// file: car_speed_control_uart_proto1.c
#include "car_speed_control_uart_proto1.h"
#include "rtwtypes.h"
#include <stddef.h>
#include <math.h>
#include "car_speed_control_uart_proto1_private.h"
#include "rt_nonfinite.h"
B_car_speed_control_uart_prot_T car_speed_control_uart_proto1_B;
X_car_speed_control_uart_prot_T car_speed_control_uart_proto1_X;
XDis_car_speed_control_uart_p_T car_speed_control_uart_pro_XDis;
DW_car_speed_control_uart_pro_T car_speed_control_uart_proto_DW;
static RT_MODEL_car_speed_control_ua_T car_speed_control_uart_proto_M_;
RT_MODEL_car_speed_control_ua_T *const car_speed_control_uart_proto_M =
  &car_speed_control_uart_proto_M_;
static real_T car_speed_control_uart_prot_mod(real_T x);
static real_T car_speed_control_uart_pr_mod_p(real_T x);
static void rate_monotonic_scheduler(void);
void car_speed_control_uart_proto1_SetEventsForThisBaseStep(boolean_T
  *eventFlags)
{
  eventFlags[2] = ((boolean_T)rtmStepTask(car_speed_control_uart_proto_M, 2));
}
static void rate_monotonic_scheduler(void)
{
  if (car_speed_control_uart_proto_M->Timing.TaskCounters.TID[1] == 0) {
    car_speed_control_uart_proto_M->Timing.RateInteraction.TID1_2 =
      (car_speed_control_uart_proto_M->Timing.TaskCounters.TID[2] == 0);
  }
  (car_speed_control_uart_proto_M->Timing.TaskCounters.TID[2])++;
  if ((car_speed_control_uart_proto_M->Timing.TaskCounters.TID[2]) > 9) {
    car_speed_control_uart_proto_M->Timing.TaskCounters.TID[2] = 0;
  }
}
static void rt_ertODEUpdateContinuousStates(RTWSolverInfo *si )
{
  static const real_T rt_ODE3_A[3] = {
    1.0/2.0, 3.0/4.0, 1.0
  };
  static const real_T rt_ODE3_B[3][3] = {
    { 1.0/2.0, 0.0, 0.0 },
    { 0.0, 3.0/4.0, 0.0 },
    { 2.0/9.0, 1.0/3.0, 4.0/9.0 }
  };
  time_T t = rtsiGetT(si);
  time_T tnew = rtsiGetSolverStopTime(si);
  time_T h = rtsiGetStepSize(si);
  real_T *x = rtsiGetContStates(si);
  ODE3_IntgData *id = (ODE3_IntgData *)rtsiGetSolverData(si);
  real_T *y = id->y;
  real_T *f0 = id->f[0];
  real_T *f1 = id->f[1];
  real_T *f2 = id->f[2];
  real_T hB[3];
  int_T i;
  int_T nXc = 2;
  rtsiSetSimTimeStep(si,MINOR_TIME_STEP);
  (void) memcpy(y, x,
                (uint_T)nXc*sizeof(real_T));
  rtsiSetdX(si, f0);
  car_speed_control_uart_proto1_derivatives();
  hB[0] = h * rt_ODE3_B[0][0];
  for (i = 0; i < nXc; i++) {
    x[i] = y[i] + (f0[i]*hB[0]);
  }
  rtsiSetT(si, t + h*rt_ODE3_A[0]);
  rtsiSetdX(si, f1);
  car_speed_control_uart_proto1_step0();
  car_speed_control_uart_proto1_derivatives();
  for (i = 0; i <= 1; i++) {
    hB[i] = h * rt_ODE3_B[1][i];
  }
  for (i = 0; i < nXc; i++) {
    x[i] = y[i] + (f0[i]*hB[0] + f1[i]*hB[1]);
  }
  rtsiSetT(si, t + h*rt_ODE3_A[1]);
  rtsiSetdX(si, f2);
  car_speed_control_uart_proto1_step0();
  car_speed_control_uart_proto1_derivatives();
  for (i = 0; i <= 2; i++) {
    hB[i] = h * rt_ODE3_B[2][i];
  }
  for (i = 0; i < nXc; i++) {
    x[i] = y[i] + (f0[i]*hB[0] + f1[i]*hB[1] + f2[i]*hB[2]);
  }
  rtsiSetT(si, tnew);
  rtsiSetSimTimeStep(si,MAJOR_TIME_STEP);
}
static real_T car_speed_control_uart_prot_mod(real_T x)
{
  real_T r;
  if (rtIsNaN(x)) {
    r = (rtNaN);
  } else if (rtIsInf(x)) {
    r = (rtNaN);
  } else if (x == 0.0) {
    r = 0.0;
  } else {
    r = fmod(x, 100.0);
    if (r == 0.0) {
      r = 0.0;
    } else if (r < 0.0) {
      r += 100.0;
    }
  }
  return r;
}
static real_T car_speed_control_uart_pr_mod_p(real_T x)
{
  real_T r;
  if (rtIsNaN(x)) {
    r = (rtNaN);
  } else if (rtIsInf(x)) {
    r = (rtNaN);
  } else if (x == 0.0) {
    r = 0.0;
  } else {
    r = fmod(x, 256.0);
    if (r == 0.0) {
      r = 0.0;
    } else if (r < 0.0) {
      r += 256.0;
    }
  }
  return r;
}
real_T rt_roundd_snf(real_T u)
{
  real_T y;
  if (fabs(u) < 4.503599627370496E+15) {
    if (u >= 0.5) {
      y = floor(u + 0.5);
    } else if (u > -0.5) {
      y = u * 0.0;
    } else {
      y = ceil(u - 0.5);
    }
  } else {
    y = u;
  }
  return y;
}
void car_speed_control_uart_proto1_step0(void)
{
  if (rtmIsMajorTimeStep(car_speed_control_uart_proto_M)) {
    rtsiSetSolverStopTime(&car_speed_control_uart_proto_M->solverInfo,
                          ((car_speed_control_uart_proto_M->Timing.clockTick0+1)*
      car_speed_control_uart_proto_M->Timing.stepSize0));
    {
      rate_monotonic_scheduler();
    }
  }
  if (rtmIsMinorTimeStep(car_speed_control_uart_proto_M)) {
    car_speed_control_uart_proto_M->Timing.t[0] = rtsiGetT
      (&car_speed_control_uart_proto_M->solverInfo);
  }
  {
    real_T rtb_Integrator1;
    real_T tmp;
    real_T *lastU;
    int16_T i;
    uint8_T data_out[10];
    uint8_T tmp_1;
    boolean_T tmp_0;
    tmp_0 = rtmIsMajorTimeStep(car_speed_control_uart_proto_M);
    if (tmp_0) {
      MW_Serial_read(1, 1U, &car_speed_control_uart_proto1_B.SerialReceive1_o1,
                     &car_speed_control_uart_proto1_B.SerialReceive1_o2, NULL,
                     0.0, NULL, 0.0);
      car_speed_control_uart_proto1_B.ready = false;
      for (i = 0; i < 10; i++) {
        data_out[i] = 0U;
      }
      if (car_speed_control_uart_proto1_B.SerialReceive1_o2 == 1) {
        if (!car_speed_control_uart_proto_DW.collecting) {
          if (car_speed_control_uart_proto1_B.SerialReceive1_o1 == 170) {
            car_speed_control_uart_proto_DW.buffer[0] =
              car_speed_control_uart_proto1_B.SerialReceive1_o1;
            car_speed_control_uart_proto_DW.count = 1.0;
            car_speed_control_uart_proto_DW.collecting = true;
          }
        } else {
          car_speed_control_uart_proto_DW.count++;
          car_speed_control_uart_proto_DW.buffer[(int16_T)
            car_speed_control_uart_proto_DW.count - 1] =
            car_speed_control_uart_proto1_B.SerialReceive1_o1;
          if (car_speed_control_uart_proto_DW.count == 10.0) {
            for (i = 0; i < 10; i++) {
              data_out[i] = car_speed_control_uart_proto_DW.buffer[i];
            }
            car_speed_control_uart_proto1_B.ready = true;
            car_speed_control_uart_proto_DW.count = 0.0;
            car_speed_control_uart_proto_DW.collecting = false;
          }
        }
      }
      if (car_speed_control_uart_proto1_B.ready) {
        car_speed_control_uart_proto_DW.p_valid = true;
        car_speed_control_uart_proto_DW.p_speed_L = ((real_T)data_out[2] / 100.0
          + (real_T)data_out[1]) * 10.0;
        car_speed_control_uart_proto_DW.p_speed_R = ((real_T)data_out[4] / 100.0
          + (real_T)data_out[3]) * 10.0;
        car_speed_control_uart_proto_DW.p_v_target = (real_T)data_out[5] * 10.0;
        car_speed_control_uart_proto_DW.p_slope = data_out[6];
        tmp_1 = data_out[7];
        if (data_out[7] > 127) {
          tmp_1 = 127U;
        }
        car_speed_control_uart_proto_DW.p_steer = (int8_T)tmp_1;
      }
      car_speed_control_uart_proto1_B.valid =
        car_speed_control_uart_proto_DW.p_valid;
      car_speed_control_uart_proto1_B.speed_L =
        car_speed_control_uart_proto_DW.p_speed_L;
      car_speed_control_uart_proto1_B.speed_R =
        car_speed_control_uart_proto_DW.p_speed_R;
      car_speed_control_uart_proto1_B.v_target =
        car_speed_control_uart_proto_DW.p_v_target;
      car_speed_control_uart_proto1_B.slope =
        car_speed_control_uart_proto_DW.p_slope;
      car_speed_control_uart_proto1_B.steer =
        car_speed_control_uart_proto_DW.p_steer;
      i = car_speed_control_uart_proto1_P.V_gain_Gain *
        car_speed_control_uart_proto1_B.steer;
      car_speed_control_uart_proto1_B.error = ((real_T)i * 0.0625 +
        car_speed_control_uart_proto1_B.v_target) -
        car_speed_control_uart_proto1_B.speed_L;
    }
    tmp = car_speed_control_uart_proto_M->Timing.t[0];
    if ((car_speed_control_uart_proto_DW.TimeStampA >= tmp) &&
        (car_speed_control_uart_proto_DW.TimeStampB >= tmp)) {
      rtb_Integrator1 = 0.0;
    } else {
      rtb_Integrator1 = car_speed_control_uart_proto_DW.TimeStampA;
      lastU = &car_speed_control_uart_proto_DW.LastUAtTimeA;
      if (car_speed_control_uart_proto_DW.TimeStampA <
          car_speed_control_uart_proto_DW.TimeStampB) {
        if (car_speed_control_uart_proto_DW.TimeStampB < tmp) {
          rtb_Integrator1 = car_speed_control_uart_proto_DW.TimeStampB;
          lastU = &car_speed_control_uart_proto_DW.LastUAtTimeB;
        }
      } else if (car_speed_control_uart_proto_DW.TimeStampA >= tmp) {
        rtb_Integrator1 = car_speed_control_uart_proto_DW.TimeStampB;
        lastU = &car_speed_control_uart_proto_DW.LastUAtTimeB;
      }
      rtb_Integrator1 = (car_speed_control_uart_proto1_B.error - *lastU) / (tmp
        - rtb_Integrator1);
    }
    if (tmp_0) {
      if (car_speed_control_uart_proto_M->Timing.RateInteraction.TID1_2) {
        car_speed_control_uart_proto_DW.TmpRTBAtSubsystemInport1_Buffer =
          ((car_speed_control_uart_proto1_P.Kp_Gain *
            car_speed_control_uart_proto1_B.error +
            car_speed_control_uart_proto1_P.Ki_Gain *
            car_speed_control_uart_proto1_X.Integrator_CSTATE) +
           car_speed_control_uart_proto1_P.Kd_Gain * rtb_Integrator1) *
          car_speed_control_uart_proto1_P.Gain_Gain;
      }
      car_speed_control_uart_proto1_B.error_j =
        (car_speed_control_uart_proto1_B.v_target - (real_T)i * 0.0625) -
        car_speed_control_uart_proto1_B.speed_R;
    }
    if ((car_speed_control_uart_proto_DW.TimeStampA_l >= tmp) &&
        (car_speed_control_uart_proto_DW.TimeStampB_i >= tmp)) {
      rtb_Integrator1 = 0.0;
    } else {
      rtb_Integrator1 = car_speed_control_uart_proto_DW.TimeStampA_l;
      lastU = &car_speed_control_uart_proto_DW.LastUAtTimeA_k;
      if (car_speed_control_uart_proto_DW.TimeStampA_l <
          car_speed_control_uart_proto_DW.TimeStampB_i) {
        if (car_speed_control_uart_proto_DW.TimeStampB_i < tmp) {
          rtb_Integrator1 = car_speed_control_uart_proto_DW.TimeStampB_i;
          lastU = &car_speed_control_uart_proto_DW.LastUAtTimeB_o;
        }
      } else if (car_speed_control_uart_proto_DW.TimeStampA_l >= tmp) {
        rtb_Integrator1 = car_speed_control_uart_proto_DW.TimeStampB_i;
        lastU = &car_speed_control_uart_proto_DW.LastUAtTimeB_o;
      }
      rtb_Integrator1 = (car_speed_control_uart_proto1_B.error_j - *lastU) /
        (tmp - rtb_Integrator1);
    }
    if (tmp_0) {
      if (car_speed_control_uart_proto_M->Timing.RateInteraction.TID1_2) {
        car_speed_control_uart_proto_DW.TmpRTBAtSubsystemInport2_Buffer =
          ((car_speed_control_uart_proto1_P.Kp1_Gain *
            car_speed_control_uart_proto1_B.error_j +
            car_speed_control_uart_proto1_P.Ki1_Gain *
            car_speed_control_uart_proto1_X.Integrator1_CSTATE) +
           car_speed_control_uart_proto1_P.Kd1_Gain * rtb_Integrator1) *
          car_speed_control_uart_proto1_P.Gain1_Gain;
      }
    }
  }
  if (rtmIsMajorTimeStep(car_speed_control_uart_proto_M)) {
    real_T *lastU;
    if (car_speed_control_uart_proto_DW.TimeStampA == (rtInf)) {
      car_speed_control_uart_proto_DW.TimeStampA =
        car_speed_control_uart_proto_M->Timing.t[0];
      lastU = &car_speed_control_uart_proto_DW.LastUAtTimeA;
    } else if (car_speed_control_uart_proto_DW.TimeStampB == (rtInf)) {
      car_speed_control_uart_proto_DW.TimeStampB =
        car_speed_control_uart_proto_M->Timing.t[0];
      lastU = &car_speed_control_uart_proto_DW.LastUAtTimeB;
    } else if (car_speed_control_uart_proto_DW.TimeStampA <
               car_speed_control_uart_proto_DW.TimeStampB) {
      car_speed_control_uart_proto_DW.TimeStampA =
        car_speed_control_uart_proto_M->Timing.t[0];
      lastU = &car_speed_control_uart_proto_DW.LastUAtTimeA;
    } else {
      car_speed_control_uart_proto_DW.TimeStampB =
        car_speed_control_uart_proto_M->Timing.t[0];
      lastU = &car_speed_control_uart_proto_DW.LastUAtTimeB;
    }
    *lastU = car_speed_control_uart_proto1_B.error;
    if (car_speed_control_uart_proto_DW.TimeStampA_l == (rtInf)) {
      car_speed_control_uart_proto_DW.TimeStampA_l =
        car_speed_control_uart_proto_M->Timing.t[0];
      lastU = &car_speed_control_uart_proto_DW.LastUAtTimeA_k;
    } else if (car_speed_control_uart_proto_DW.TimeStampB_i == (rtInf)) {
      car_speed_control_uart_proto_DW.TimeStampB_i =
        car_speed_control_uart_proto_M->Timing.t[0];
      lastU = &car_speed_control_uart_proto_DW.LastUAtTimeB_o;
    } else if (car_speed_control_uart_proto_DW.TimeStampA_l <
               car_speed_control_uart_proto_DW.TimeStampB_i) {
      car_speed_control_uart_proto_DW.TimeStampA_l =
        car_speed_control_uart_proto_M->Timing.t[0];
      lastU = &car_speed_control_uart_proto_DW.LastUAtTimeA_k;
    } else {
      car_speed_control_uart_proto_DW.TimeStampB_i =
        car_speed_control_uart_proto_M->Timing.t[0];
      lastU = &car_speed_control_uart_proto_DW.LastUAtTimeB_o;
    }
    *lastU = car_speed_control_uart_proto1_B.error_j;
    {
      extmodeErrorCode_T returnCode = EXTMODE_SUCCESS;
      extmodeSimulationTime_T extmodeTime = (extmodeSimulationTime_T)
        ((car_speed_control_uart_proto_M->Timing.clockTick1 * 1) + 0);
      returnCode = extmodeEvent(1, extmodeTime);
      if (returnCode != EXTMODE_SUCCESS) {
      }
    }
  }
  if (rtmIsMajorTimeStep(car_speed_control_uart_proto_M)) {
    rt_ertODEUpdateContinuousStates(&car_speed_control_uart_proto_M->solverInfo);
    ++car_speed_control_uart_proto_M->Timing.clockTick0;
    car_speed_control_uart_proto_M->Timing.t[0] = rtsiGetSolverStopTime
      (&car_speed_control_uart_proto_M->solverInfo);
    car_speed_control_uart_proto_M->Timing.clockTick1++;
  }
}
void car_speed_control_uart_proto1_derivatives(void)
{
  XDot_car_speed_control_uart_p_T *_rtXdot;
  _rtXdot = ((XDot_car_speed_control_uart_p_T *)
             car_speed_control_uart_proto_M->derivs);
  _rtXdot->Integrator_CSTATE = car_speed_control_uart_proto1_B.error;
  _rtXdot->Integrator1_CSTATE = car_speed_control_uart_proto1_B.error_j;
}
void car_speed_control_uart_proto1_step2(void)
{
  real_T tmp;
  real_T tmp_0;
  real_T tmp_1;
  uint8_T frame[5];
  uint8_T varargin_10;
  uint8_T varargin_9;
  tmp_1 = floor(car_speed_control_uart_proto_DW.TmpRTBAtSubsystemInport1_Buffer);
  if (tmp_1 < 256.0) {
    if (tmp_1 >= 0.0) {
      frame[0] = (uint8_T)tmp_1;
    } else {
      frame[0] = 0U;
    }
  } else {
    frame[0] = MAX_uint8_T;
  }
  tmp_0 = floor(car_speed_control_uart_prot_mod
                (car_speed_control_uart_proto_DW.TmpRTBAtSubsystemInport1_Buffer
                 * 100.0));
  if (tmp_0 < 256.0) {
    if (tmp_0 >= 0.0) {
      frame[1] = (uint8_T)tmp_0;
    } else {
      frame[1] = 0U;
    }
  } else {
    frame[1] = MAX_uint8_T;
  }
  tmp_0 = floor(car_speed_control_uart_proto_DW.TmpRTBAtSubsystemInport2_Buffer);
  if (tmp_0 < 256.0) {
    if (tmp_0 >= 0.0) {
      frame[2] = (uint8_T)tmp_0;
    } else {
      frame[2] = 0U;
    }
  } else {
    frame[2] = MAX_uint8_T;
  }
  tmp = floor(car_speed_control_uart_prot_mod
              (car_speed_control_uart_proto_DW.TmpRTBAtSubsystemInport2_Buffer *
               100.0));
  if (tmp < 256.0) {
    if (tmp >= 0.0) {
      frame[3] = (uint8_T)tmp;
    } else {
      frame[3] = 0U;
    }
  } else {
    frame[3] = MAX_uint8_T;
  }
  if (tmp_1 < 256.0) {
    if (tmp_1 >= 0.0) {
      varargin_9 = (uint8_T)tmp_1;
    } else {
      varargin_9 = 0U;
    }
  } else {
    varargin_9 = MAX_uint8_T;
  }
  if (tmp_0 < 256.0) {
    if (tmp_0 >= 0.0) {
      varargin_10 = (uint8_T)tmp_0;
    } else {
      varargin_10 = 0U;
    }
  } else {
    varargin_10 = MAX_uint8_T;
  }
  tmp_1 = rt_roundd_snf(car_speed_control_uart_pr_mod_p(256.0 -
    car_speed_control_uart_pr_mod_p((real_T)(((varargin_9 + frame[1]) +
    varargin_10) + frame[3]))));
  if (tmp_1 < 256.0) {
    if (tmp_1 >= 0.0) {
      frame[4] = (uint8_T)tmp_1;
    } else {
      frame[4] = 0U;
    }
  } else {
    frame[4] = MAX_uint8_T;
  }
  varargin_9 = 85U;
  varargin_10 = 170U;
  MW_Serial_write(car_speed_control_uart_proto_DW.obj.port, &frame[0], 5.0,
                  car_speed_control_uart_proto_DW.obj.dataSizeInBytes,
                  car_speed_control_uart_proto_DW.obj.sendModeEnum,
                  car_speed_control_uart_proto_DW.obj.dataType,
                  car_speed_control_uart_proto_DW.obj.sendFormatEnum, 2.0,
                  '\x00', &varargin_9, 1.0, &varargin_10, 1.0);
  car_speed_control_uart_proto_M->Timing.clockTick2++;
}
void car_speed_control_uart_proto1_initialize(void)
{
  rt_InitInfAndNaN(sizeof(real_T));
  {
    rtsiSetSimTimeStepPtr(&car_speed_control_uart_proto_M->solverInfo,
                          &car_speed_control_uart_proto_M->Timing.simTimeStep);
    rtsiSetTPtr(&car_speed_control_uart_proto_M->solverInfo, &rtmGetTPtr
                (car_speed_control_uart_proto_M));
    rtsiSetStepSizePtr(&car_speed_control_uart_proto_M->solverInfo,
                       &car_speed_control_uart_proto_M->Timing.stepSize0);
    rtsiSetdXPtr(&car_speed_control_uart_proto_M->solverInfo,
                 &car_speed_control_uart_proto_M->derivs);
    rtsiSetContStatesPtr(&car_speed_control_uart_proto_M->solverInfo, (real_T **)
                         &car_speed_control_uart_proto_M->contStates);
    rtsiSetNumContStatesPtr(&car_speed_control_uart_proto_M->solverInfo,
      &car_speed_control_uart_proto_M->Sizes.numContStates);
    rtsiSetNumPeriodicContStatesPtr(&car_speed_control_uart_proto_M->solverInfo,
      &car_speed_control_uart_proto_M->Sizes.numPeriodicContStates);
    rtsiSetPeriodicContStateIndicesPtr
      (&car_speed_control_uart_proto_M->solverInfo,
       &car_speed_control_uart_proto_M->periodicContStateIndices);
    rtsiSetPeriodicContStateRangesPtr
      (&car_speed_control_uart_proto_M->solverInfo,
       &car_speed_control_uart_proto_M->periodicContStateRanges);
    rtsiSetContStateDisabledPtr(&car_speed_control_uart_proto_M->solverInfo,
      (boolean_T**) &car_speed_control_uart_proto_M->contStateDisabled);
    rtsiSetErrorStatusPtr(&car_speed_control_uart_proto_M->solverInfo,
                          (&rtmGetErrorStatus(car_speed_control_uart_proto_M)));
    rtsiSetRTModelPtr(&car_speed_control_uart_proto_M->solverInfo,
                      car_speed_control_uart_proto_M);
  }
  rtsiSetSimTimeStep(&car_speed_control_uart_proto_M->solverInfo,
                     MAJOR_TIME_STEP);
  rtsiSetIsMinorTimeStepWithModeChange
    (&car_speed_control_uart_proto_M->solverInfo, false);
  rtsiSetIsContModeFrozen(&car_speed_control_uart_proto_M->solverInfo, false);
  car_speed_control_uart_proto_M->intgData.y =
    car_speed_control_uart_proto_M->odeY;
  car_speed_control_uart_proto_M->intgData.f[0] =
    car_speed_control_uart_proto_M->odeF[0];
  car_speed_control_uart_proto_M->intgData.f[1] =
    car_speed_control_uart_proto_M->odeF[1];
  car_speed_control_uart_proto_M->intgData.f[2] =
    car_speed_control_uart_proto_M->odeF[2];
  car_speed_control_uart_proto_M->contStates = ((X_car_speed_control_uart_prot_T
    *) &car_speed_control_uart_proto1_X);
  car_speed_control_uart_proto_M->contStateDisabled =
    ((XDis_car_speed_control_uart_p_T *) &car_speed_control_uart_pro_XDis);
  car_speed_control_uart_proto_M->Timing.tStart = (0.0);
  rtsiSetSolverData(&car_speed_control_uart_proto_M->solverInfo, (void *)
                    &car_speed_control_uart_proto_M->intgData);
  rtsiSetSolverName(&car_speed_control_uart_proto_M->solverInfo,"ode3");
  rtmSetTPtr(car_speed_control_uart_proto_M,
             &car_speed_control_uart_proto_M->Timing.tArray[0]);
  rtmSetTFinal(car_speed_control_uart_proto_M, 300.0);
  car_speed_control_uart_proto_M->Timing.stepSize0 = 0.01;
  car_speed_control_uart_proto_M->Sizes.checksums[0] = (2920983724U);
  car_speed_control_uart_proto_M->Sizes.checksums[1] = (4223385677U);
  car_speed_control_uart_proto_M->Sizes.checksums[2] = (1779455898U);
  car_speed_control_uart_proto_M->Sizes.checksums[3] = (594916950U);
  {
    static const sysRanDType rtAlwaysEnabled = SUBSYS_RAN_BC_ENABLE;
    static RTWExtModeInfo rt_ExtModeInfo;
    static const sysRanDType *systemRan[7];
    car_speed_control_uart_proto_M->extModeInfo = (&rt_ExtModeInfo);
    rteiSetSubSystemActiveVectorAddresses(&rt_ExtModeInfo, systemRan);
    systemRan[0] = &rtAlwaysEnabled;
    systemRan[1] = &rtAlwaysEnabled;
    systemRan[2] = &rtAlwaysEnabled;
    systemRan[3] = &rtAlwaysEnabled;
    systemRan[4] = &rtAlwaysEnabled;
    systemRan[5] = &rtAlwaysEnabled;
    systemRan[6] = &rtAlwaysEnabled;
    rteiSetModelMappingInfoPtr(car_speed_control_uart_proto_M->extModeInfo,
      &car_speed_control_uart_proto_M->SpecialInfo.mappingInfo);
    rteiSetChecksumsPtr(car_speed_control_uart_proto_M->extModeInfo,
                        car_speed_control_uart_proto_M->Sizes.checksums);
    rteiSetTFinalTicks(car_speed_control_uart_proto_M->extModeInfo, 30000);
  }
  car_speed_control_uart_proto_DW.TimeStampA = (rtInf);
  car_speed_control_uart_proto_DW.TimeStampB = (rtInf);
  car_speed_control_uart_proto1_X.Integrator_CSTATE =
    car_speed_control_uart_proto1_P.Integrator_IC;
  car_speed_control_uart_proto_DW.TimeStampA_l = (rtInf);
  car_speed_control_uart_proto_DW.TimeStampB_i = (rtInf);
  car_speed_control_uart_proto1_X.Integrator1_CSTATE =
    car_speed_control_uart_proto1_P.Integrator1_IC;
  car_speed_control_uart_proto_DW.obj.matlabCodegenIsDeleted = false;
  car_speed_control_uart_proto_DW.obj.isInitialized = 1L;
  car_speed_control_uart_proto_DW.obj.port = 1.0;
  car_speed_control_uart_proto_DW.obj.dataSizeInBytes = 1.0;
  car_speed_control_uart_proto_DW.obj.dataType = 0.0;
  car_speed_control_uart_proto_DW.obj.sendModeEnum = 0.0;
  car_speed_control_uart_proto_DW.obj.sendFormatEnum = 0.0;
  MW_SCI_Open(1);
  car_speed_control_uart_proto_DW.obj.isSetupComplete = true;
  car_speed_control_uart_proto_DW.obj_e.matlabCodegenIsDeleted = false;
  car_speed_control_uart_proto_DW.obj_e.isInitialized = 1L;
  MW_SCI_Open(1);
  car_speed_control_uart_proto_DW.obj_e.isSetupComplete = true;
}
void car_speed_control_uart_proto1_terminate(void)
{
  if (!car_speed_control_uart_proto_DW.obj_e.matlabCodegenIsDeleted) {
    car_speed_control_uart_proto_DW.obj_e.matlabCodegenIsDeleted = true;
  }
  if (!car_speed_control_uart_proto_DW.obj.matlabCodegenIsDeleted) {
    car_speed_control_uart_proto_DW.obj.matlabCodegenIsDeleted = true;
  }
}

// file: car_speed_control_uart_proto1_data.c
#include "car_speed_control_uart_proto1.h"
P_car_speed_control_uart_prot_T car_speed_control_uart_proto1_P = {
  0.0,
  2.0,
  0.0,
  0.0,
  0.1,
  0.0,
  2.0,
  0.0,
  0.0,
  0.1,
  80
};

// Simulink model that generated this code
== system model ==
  Subsystem#1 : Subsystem  <- 1: Gain, 2: Gain1
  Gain : Gain  Gain=0.1  <- 1: Sum#1
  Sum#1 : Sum  Inputs=+++  <- 1: Kp, 2: Ki, 3: Kd
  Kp : Gain  Gain=2  <- 1: Sum#2
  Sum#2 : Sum  Inputs=+-  <- 1: Sum#3, 2: MATLABFunction#1/2
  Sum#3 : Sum  Inputs=++  <- 1: MATLABFunction#1/4, 2: V_gain
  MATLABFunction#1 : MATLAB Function  <- 1: MATLABFunction#2, 2: MATLABFunction#2/2
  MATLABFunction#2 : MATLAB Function  <- 1: SerialReceive1, 2: SerialReceive1/2
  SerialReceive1 : arduinolib/Serial Receive
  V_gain : Gain  Gain=5  <- 1: MATLABFunction#1/6
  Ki : Gain  Gain=0  <- 1: Integrator
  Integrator : Integrator  <- 1: Sum#2
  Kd : Gain  Gain=0  <- 1: Derivative#1
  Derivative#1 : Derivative  <- 1: Sum#2
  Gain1 : Gain  Gain=0.1  <- 1: Sum#4
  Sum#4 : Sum  Inputs=+++  <- 1: Kp1, 2: Ki1, 3: Kd1
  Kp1 : Gain  Gain=2  <- 1: Sum#5
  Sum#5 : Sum  Inputs=+-  <- 1: Sum#6, 2: MATLABFunction#1/3
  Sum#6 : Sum  Inputs=+-  <- 1: MATLABFunction#1/4, 2: V_gain
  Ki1 : Gain  Gain=0  <- 1: Integrator1
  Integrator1 : Integrator  <- 1: Sum#5
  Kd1 : Gain  Gain=0  <- 1: Derivative#2
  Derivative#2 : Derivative  <- 1: Sum#5
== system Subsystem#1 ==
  Inport#1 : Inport
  Inport#2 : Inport
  SerialTransmit#1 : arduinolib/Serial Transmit  <- 1: MATLABFunction#3
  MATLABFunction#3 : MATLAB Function  <- 1: Inport#1, 2: Inport#2
== matlab function MATLABFunction#1 ==
function [valid, speed_L, speed_R, v_target, slope, steer] = parseUART_persistent(ready, u)
% UART 패킷 파서 (persistent 방식으로 이전 값 유지)
% u: [10x1] uint8, 패킷 데이터
% ready: 패킷 유효 신호

%#codegen

% 이전 출력값 저장용 persistent 변수
persistent p_valid p_speed_L p_speed_R p_v_target p_slope p_steer

% 초기화 (최초 실행 시)
if isempty(p_valid)
    p_valid = false;
    p_speed_L = 0.0;
    p_speed_R = 0.0;
    p_v_target = 0.0;
    p_slope = uint8(0);
    p_steer = int8(0);
end

% 새로운 데이터가 들어왔을 경우만 업데이트
if ready == 1
        p_valid = true;
        p_speed_L = (double(u(2)) + double(u(3))/100) * 10;
        p_speed_R = (double(u(4)) + double(u(5))/100) * 10;
        p_v_target = double(u(6))*10;
        p_slope = u(7);
        p_steer = int8(u(8));
end

% 항상 마지막 유효 출력 반환
valid     = p_valid;
speed_L   = p_speed_L;
speed_R   = p_speed_R;
v_target  = p_v_target;
slope     = p_slope;
steer     = p_steer;

== matlab function MATLABFunction#2 ==
function [ready, data_out] = uart_parser(byte_in, status)
% UART 프레임 수신기 (Start Byte = 0xAA, Total = 10 bytes)
% 입력: byte_in - 1바이트씩 들어오는 uint8
% 입력: status - Serial Receive의 상태 (1이면 수신 성공)
% 출력: ready - 1이면 패킷 파싱 완료
% 출력: data_out - [1x10] uint8, 패킷 데이터

persistent buffer count collecting

if isempty(buffer)
    buffer = zeros(1, 10, 'uint8');
    count = 0;
    collecting = false;
end

ready = false;
data_out = zeros(1,10,'uint8');

if status == 1
    if ~collecting
        % 아직 수집 시작 전 → start byte 찾기
        if byte_in == hex2dec('AA')
            buffer(1) = byte_in;
            count = 1;
            collecting = true;
        end
    else
        % 수집 중
        count = count + 1;
        buffer(count) = byte_in;

        if count == 10
            data_out = buffer;
            ready = true;
            count = 0;
            collecting = false;
        end
    end
end

== matlab function MATLABFunction#3 ==
function frame = makeFrame(vL, vR)
% 입력:
%   vL, vR : 좌/우 목표 속도 (실수, cm/s 단위)
% 출력:
%   frame : 7-byte UART 전송 프레임 (uint8 벡터)
    frame = zeros(5,1,'uint8');  % 7바이트 프레임

    % 2-3. 목표속도_L (정수 + 소수)
    frame(1) = uint8(floor(vL));                       % 정수부
    frame(2) = uint8(floor(mod(vL * 100, 100)));       % 소수부 (소수점 둘째 자리까지)

    % 4-5. 목표속도_R (정수 + 소수)
    frame(3) = uint8(floor(vR));                       % 정수부
    frame(4) = uint8(floor(mod(vR * 100, 100)));       % 소수부

    % 6. CRC: 256 - (sum of byte 1~5) % 256
    crc = mod(sum(double(frame(1:5))), 256);
    frame(5) = uint8(mod(256 - crc, 256));
    
end
